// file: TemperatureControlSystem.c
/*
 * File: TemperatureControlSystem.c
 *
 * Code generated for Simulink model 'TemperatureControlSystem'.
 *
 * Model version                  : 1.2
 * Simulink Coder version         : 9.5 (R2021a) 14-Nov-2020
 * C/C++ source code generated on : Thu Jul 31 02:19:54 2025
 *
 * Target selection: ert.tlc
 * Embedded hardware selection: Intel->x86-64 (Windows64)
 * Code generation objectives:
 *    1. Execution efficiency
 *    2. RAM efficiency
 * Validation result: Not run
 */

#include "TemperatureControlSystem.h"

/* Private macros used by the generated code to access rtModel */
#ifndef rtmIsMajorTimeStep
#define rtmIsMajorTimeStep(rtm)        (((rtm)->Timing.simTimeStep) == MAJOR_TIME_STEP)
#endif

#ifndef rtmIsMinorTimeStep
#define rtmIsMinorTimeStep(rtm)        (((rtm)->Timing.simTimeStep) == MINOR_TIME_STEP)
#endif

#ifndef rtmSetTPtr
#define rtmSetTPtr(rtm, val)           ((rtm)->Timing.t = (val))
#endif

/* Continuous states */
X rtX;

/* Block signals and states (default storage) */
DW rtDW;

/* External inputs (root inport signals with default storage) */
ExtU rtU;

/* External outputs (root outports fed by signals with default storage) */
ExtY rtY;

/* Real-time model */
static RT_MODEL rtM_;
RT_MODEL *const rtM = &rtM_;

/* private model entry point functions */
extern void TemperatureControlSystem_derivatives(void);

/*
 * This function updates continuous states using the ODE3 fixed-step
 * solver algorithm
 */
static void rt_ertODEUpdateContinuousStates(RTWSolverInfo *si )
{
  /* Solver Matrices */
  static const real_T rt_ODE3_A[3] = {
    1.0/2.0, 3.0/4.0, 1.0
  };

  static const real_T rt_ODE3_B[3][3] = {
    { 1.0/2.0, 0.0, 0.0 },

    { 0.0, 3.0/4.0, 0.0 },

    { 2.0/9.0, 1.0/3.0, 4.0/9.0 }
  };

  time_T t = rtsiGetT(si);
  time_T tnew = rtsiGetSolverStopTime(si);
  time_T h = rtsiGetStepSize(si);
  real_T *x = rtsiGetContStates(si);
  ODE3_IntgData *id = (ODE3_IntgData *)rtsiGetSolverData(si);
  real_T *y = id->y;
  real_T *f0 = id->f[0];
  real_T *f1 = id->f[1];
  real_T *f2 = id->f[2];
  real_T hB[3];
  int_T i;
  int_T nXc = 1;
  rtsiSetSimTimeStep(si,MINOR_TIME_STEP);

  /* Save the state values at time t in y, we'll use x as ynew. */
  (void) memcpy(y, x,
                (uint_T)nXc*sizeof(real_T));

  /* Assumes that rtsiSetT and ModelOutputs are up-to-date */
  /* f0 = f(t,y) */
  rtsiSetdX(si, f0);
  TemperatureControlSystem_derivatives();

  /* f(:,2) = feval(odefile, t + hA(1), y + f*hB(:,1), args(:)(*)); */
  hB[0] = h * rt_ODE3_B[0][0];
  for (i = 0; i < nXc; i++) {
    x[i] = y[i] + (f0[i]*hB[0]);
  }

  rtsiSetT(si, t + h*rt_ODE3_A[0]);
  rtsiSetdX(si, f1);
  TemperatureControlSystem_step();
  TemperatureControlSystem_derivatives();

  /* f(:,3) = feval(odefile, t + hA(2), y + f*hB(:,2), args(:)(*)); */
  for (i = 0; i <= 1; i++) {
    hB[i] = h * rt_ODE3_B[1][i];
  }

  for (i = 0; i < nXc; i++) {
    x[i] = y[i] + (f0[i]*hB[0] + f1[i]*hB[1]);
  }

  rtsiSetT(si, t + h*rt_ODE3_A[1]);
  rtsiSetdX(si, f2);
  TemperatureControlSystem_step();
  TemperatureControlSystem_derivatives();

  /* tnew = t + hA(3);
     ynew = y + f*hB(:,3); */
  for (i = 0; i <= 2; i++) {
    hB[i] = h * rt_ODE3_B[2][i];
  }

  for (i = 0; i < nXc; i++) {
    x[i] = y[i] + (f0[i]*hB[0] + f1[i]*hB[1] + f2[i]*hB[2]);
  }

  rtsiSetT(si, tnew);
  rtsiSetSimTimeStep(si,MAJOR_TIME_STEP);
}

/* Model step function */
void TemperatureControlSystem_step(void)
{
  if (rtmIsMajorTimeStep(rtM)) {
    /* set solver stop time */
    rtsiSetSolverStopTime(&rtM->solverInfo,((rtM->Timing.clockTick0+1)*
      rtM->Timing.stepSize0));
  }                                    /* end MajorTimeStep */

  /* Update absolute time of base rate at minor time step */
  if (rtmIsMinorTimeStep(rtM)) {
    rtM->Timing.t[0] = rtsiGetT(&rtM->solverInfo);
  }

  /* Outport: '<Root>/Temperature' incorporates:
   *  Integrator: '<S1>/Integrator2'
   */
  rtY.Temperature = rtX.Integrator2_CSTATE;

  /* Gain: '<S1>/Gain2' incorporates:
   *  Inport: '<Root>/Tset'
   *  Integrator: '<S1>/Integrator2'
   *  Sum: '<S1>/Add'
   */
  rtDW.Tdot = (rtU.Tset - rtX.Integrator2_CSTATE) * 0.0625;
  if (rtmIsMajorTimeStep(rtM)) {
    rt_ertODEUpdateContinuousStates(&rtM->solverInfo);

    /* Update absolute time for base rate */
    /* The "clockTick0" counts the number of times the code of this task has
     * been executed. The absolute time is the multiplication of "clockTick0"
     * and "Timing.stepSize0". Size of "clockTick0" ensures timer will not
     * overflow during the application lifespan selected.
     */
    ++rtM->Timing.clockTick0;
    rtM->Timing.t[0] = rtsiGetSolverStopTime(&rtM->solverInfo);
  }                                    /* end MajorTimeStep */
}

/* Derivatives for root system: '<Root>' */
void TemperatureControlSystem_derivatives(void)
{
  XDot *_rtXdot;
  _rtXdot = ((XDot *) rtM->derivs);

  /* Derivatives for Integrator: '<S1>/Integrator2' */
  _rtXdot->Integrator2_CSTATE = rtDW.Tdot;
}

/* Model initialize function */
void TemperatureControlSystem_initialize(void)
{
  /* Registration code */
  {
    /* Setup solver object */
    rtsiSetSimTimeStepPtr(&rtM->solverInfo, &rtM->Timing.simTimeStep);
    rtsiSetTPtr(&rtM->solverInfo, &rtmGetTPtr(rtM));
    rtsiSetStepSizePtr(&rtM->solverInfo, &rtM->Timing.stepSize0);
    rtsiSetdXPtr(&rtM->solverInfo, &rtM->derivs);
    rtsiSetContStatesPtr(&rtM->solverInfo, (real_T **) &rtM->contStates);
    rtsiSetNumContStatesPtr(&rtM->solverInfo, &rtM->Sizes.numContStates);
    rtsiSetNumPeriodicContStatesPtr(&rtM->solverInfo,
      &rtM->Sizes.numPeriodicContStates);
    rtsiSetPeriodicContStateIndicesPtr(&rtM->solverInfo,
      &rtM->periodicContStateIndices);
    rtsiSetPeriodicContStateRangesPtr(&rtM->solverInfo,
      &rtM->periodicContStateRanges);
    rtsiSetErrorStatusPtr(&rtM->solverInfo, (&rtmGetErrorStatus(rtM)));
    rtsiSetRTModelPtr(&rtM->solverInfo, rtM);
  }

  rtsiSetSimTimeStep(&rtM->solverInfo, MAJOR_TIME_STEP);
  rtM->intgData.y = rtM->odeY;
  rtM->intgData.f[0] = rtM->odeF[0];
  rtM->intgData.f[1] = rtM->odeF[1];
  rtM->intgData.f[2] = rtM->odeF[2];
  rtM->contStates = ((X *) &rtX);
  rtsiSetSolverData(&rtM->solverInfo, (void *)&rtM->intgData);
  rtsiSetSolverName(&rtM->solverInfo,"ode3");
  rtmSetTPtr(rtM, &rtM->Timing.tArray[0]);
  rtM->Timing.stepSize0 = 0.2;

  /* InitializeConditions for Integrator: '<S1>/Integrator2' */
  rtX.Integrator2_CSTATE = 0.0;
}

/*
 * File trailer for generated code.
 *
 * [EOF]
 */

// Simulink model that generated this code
simulink model "TemperatureControlSystem"  (R2021a)
settings: Solver=FixedStepAuto  StartTime=0.0  StopTime=10.0  MaxStep=0.1  RelTol=1e-3

== system TemperatureControlSystem ==
  Tset : Inport
  Temperature Control System : Subsystem
  Temperature : Outport
  wires:
  Tset/1 -> Temperature Control System/1(Tset)
  Temperature Control System/1(Temperature) -> Temperature/1

== system TemperatureControlSystem/Temperature Control System ==
  Tset : Inport
  Add : Sum  Inputs=+-
  Gain2 : Gain  Gain=Ku/ Taw
  Integrator2 : Integrator
  Temperature : Outport
  wires:
  Add/1 -> Gain2/1
  Integrator2/1 -> Temperature/1, Add/2  "T"
  Gain2/1 -> Integrator2/1  "T-dot"
  Tset/1 -> Add/1
